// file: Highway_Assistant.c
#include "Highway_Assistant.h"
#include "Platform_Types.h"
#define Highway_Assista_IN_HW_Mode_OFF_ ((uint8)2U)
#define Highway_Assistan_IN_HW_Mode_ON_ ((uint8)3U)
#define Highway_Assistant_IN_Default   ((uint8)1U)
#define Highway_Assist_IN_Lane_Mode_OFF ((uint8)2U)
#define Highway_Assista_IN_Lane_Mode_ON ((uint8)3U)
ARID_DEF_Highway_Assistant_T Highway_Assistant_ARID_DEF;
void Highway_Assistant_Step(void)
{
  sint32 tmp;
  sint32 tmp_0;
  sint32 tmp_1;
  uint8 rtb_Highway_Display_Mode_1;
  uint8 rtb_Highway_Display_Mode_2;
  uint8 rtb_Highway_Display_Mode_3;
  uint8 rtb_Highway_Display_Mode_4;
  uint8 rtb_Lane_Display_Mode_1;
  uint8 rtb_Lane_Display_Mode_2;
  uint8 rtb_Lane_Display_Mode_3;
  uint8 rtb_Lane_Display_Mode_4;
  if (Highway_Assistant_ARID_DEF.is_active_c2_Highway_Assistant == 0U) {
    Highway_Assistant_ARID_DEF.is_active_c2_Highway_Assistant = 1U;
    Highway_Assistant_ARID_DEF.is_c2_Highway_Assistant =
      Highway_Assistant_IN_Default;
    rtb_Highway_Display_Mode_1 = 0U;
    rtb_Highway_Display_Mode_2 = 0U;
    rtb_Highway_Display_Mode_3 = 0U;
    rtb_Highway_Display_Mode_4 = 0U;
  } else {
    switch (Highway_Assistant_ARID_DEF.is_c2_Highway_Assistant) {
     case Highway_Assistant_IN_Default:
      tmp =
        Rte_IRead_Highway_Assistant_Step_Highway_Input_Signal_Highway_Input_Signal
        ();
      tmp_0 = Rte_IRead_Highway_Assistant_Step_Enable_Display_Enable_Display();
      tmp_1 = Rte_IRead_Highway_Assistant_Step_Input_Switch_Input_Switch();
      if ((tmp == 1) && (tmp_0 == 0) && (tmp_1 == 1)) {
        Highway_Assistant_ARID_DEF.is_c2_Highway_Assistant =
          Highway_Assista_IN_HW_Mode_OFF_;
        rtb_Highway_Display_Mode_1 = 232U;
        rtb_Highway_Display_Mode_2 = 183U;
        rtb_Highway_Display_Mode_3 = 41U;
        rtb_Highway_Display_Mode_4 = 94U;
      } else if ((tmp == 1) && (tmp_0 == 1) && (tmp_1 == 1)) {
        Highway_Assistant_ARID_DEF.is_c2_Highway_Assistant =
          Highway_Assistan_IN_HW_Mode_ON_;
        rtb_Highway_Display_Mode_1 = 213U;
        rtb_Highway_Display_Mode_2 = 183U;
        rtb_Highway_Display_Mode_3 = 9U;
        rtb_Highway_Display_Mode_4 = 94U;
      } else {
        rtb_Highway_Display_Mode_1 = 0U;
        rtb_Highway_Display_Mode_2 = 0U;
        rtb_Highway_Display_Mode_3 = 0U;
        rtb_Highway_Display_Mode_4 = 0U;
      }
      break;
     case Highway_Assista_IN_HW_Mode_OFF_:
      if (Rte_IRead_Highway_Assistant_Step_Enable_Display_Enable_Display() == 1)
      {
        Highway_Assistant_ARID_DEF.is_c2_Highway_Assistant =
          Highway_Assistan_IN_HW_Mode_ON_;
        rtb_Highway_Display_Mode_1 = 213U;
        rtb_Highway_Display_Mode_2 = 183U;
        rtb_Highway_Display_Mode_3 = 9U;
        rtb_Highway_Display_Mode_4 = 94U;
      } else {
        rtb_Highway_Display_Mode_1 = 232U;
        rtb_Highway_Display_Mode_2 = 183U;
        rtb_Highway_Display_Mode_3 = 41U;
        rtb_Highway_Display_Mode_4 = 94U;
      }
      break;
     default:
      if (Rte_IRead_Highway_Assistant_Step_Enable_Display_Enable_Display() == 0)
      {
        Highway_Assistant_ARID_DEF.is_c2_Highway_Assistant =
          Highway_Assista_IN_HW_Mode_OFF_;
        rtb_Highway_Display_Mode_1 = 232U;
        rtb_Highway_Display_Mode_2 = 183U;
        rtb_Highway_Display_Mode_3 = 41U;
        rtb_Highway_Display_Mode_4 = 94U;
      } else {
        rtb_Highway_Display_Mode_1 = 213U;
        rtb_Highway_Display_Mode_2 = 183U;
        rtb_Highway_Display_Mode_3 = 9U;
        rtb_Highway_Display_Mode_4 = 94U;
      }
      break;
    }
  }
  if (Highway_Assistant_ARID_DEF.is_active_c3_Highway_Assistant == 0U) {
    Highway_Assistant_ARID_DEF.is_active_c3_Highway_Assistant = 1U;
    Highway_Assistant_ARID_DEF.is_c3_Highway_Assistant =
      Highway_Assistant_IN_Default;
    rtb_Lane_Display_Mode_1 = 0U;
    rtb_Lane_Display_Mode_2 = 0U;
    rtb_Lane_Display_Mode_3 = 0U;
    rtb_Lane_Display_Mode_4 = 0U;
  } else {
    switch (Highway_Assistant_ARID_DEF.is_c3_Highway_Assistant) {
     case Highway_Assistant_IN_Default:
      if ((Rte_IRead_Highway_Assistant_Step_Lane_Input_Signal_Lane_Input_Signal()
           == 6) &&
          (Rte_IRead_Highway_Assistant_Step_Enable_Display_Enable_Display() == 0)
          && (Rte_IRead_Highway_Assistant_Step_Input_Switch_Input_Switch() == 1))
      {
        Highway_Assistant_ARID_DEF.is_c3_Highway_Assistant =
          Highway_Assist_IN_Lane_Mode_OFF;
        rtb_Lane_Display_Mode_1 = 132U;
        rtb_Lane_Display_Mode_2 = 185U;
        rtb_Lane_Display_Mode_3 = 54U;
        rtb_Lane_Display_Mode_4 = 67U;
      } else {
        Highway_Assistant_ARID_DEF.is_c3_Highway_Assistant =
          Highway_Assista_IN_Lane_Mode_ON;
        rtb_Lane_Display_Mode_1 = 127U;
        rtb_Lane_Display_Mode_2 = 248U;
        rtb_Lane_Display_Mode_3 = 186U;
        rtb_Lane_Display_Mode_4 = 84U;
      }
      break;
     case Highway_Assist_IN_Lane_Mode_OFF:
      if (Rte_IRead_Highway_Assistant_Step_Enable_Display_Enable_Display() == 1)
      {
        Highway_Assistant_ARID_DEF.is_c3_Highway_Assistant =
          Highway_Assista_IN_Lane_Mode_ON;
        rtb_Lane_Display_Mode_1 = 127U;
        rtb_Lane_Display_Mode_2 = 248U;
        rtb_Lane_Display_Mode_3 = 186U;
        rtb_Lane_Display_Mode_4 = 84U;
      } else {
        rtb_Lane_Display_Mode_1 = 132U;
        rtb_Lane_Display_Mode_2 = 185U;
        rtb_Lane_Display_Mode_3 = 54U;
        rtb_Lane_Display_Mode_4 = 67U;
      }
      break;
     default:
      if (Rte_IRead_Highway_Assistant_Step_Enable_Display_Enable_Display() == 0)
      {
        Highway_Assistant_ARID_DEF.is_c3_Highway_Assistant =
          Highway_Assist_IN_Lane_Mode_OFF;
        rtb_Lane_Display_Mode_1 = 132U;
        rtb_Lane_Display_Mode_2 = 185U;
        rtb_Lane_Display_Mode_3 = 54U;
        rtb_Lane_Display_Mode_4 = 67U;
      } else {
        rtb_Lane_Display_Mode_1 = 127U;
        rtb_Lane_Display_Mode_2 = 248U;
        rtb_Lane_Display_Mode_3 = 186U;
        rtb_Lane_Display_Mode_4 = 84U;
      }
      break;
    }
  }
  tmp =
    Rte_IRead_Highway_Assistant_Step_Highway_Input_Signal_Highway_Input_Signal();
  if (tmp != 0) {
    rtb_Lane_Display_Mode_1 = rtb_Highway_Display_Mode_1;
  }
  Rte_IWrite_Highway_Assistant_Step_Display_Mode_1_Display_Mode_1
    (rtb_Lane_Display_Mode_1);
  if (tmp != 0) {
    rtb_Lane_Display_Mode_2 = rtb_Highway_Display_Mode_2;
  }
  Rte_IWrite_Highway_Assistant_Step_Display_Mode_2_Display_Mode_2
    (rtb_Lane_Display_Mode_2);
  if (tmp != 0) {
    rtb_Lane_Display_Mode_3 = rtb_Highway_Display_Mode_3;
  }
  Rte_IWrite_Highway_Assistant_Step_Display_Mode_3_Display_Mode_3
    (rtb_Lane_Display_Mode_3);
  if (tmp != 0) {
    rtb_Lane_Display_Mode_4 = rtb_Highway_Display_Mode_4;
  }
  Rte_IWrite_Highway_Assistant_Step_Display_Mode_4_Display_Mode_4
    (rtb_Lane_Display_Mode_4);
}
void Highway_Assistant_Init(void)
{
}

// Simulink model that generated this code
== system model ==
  Highway_Input_Signal : Inport
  Input_Switch : Inport
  Enable_Display : Inport
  Lane_Input_Signal : Inport
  Display_Mode_1 : Outport  <- 1: Switch
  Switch : Switch  Criteria=u2 ~= 0  <- 1: Stateflowchart#1/2, 2: Highway_Input_Signal, 3: Stateflowchart#2
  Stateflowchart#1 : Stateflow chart  <- 1: Highway_Input_Signal, 2: Input_Switch, 3: Enable_Display
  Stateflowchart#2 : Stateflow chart  <- 1: Lane_Input_Signal, 2: Input_Switch, 3: Enable_Display
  Display_Mode_2 : Outport  <- 1: Switch#1
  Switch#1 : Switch  Criteria=u2 ~= 0  <- 1: Stateflowchart#1/4, 2: Highway_Input_Signal, 3: Stateflowchart#2/2
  Display_Mode_3 : Outport  <- 1: Switch#2
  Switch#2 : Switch  Criteria=u2 ~= 0  <- 1: Stateflowchart#1, 2: Highway_Input_Signal, 3: Stateflowchart#2/3
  Display_Mode_4 : Outport  <- 1: Switch#3
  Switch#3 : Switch  Criteria=u2 ~= 0  <- 1: Stateflowchart#1/3, 2: Highway_Input_Signal, 3: Stateflowchart#2/4
== stateflow chart Stateflowchart#1 ==
  state Default
    Highway_Display_Mode_1 = 0;
    Highway_Display_Mode_2 = 0;
    Highway_Display_Mode_3 = 0;
    Highway_Display_Mode_4 = 0;
  state HW_Mode_ON_
    Highway_Display_Mode_1 = 213;
    Highway_Display_Mode_2 = 183;
    Highway_Display_Mode_3 = 9;
    Highway_Display_Mode_4 = 94;
  state HW_Mode_OFF_
    Highway_Display_Mode_1 = 232;
    Highway_Display_Mode_2 = 183;
    Highway_Display_Mode_3 = 41;
    Highway_Display_Mode_4 = 94;
  (default) -> Default
  Default -> HW_Mode_OFF_ [order 1] : [Highway_Input_Signal == 1 && Enable_Display == 0 && Input_Switch == 1]
  Default -> HW_Mode_ON_ [order 2] : [Highway_Input_Signal == 1 && Enable_Display == 1 && Input_Switch == 1]
  HW_Mode_OFF_ -> HW_Mode_ON_ [order 1] : [Enable_Display == 1]
  HW_Mode_ON_ -> HW_Mode_OFF_ [order 1] : [Enable_Display == 0]
  HW_Mode_ON_ -> (junction 6) [order 2]
  HW_Mode_OFF_ -> (junction 5) [order 2]
  data: Highway_Display_Mode_3 output uint8; Highway_Input_Signal input; Input_Switch input; Enable_Display input; Highway_Display_Mode_1 output uint8; Highway_Display_Mode_4 output uint8; Highway_Display_Mode_2 output uint8

== stateflow chart Stateflowchart#2 ==
  state Default
    Lane_Display_Mode_1 = 0;
    Lane_Display_Mode_2 = 0;
    Lane_Display_Mode_3 = 0;
    Lane_Display_Mode_4 = 0;
  note: [Lane_Input_Signal == 6 && Enable_Display == 1 && Input_Switch == 1]
  state Lane_Mode_ON
    Lane_Display_Mode_1 = 127;
    Lane_Display_Mode_2 = 248;
    Lane_Display_Mode_3 = 186;
    Lane_Display_Mode_4 = 84;
  state Lane_Mode_OFF
    Lane_Display_Mode_1 = 132;
    Lane_Display_Mode_2 = 185;
    Lane_Display_Mode_3 = 54;
    Lane_Display_Mode_4 = 67;
  (default) -> Default
  Default -> state1 [order 1] : [Lane_Input_Signal == 6 && Enable_Display == 0 && Input_Switch == 1]
  Default -> state4 [order 2]
  state1 -> state4 [order 1] : [Enable_Display == 1]
  state4 -> state1 [order 1] : [Enable_Display == 0]
  state1 -> (junction 15) [order 2]
  state4 -> (junction 5) [order 2]
  data: Lane_Input_Signal input uint8; Input_Switch input uint8; Lane_Display_Mode_1 output uint8; Lane_Display_Mode_2 output uint8; Lane_Display_Mode_3 output uint8; Enable_Display input uint8; Lane_Display_Mode_4 output uint8
